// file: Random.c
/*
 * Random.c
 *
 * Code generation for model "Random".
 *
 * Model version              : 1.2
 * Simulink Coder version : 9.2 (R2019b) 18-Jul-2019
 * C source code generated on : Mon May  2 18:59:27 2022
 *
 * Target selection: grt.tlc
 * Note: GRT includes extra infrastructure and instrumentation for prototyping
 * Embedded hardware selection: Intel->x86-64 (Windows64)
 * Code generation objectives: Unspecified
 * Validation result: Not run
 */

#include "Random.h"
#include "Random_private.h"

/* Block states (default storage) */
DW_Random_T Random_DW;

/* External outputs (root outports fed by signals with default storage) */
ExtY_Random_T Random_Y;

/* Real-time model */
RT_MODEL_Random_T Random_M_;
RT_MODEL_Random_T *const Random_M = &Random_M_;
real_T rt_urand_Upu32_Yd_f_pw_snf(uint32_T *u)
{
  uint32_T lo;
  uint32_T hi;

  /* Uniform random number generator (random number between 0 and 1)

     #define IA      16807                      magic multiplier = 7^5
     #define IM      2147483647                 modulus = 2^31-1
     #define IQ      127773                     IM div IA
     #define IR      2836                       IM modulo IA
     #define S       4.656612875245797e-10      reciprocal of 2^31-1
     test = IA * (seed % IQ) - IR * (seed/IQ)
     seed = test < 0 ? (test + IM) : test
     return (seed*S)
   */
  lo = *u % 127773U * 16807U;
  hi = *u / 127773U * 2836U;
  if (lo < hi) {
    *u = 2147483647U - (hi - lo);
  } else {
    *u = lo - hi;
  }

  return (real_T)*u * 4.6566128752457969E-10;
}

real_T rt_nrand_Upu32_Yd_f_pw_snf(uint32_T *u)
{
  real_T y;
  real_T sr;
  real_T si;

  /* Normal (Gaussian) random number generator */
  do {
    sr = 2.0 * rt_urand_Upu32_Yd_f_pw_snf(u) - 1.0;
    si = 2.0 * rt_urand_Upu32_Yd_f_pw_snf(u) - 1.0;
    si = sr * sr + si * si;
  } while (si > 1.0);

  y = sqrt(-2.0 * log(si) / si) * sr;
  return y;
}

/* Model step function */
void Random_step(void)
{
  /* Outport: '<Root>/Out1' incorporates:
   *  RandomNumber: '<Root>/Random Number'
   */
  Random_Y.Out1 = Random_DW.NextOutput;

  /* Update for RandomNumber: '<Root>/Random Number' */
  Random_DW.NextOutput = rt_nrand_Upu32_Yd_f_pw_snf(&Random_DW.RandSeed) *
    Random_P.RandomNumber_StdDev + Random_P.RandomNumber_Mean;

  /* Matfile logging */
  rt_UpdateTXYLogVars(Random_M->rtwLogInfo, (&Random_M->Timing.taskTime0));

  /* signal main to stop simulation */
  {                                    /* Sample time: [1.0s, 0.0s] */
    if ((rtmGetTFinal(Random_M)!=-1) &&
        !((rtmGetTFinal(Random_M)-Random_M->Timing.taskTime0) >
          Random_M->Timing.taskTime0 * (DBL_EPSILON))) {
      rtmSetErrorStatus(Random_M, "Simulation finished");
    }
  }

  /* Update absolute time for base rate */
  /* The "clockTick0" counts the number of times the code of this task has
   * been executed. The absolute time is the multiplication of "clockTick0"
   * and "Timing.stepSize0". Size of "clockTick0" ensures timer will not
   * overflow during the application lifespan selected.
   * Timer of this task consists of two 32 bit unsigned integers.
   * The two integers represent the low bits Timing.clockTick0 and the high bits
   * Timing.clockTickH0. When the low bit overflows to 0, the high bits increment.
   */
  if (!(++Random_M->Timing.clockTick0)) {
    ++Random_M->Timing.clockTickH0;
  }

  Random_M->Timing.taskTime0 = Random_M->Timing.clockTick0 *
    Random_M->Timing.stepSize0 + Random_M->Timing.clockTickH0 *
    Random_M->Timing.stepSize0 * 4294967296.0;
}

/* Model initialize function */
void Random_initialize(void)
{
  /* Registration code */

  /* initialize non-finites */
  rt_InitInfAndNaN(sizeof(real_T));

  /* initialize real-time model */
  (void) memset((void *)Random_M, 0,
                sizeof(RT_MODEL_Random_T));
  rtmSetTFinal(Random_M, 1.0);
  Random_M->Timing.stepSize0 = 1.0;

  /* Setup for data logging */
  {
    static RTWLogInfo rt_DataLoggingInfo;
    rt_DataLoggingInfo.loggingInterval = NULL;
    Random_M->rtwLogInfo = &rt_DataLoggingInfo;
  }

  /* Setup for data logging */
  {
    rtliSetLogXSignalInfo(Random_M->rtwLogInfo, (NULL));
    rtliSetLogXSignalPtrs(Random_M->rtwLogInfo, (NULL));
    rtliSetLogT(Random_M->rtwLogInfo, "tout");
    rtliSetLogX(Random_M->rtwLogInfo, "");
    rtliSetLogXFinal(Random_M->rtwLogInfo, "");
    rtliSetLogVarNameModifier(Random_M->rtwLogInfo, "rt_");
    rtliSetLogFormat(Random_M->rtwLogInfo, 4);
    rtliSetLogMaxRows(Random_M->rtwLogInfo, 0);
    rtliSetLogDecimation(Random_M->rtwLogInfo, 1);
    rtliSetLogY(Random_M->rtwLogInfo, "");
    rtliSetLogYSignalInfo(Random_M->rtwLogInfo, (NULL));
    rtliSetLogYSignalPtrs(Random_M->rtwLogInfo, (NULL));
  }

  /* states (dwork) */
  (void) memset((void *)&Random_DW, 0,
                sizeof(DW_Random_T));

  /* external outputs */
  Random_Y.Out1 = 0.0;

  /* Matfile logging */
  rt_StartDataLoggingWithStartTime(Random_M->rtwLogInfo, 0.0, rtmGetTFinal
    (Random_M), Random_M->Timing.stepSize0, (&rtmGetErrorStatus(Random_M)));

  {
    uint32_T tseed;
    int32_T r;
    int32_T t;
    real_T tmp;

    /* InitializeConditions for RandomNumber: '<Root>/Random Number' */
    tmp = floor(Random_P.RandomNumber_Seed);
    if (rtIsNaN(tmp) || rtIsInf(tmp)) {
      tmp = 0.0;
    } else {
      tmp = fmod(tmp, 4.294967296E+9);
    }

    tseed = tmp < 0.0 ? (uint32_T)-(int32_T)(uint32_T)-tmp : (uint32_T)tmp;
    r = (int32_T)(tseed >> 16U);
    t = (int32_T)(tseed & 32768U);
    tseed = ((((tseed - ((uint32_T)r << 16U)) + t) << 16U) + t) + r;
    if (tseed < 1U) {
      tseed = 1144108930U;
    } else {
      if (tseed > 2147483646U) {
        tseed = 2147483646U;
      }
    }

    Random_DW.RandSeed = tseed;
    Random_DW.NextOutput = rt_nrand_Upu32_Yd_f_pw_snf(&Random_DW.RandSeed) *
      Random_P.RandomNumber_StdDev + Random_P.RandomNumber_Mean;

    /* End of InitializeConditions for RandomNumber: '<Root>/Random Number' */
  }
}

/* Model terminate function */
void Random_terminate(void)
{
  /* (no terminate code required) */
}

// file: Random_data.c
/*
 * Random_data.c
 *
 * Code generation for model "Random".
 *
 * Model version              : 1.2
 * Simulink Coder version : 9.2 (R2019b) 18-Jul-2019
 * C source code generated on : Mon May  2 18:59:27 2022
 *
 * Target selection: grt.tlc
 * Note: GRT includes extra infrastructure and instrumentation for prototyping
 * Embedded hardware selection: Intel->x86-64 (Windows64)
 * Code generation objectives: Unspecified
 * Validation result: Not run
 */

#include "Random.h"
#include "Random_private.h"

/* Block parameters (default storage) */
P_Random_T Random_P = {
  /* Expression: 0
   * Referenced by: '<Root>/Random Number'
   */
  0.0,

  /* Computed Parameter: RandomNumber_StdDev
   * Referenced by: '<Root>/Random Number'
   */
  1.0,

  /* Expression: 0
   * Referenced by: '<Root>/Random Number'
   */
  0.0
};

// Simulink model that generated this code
simulink model "Random"  (R2019b)
settings: Solver=FixedStepAuto  StartTime=0.0  StopTime=1  RelTol=1e-3

== system Random ==
  Random Number : RandomNumber  SampleTime=1
  Out1 : Outport
  wires:
  Random Number/1 -> Out1/1
